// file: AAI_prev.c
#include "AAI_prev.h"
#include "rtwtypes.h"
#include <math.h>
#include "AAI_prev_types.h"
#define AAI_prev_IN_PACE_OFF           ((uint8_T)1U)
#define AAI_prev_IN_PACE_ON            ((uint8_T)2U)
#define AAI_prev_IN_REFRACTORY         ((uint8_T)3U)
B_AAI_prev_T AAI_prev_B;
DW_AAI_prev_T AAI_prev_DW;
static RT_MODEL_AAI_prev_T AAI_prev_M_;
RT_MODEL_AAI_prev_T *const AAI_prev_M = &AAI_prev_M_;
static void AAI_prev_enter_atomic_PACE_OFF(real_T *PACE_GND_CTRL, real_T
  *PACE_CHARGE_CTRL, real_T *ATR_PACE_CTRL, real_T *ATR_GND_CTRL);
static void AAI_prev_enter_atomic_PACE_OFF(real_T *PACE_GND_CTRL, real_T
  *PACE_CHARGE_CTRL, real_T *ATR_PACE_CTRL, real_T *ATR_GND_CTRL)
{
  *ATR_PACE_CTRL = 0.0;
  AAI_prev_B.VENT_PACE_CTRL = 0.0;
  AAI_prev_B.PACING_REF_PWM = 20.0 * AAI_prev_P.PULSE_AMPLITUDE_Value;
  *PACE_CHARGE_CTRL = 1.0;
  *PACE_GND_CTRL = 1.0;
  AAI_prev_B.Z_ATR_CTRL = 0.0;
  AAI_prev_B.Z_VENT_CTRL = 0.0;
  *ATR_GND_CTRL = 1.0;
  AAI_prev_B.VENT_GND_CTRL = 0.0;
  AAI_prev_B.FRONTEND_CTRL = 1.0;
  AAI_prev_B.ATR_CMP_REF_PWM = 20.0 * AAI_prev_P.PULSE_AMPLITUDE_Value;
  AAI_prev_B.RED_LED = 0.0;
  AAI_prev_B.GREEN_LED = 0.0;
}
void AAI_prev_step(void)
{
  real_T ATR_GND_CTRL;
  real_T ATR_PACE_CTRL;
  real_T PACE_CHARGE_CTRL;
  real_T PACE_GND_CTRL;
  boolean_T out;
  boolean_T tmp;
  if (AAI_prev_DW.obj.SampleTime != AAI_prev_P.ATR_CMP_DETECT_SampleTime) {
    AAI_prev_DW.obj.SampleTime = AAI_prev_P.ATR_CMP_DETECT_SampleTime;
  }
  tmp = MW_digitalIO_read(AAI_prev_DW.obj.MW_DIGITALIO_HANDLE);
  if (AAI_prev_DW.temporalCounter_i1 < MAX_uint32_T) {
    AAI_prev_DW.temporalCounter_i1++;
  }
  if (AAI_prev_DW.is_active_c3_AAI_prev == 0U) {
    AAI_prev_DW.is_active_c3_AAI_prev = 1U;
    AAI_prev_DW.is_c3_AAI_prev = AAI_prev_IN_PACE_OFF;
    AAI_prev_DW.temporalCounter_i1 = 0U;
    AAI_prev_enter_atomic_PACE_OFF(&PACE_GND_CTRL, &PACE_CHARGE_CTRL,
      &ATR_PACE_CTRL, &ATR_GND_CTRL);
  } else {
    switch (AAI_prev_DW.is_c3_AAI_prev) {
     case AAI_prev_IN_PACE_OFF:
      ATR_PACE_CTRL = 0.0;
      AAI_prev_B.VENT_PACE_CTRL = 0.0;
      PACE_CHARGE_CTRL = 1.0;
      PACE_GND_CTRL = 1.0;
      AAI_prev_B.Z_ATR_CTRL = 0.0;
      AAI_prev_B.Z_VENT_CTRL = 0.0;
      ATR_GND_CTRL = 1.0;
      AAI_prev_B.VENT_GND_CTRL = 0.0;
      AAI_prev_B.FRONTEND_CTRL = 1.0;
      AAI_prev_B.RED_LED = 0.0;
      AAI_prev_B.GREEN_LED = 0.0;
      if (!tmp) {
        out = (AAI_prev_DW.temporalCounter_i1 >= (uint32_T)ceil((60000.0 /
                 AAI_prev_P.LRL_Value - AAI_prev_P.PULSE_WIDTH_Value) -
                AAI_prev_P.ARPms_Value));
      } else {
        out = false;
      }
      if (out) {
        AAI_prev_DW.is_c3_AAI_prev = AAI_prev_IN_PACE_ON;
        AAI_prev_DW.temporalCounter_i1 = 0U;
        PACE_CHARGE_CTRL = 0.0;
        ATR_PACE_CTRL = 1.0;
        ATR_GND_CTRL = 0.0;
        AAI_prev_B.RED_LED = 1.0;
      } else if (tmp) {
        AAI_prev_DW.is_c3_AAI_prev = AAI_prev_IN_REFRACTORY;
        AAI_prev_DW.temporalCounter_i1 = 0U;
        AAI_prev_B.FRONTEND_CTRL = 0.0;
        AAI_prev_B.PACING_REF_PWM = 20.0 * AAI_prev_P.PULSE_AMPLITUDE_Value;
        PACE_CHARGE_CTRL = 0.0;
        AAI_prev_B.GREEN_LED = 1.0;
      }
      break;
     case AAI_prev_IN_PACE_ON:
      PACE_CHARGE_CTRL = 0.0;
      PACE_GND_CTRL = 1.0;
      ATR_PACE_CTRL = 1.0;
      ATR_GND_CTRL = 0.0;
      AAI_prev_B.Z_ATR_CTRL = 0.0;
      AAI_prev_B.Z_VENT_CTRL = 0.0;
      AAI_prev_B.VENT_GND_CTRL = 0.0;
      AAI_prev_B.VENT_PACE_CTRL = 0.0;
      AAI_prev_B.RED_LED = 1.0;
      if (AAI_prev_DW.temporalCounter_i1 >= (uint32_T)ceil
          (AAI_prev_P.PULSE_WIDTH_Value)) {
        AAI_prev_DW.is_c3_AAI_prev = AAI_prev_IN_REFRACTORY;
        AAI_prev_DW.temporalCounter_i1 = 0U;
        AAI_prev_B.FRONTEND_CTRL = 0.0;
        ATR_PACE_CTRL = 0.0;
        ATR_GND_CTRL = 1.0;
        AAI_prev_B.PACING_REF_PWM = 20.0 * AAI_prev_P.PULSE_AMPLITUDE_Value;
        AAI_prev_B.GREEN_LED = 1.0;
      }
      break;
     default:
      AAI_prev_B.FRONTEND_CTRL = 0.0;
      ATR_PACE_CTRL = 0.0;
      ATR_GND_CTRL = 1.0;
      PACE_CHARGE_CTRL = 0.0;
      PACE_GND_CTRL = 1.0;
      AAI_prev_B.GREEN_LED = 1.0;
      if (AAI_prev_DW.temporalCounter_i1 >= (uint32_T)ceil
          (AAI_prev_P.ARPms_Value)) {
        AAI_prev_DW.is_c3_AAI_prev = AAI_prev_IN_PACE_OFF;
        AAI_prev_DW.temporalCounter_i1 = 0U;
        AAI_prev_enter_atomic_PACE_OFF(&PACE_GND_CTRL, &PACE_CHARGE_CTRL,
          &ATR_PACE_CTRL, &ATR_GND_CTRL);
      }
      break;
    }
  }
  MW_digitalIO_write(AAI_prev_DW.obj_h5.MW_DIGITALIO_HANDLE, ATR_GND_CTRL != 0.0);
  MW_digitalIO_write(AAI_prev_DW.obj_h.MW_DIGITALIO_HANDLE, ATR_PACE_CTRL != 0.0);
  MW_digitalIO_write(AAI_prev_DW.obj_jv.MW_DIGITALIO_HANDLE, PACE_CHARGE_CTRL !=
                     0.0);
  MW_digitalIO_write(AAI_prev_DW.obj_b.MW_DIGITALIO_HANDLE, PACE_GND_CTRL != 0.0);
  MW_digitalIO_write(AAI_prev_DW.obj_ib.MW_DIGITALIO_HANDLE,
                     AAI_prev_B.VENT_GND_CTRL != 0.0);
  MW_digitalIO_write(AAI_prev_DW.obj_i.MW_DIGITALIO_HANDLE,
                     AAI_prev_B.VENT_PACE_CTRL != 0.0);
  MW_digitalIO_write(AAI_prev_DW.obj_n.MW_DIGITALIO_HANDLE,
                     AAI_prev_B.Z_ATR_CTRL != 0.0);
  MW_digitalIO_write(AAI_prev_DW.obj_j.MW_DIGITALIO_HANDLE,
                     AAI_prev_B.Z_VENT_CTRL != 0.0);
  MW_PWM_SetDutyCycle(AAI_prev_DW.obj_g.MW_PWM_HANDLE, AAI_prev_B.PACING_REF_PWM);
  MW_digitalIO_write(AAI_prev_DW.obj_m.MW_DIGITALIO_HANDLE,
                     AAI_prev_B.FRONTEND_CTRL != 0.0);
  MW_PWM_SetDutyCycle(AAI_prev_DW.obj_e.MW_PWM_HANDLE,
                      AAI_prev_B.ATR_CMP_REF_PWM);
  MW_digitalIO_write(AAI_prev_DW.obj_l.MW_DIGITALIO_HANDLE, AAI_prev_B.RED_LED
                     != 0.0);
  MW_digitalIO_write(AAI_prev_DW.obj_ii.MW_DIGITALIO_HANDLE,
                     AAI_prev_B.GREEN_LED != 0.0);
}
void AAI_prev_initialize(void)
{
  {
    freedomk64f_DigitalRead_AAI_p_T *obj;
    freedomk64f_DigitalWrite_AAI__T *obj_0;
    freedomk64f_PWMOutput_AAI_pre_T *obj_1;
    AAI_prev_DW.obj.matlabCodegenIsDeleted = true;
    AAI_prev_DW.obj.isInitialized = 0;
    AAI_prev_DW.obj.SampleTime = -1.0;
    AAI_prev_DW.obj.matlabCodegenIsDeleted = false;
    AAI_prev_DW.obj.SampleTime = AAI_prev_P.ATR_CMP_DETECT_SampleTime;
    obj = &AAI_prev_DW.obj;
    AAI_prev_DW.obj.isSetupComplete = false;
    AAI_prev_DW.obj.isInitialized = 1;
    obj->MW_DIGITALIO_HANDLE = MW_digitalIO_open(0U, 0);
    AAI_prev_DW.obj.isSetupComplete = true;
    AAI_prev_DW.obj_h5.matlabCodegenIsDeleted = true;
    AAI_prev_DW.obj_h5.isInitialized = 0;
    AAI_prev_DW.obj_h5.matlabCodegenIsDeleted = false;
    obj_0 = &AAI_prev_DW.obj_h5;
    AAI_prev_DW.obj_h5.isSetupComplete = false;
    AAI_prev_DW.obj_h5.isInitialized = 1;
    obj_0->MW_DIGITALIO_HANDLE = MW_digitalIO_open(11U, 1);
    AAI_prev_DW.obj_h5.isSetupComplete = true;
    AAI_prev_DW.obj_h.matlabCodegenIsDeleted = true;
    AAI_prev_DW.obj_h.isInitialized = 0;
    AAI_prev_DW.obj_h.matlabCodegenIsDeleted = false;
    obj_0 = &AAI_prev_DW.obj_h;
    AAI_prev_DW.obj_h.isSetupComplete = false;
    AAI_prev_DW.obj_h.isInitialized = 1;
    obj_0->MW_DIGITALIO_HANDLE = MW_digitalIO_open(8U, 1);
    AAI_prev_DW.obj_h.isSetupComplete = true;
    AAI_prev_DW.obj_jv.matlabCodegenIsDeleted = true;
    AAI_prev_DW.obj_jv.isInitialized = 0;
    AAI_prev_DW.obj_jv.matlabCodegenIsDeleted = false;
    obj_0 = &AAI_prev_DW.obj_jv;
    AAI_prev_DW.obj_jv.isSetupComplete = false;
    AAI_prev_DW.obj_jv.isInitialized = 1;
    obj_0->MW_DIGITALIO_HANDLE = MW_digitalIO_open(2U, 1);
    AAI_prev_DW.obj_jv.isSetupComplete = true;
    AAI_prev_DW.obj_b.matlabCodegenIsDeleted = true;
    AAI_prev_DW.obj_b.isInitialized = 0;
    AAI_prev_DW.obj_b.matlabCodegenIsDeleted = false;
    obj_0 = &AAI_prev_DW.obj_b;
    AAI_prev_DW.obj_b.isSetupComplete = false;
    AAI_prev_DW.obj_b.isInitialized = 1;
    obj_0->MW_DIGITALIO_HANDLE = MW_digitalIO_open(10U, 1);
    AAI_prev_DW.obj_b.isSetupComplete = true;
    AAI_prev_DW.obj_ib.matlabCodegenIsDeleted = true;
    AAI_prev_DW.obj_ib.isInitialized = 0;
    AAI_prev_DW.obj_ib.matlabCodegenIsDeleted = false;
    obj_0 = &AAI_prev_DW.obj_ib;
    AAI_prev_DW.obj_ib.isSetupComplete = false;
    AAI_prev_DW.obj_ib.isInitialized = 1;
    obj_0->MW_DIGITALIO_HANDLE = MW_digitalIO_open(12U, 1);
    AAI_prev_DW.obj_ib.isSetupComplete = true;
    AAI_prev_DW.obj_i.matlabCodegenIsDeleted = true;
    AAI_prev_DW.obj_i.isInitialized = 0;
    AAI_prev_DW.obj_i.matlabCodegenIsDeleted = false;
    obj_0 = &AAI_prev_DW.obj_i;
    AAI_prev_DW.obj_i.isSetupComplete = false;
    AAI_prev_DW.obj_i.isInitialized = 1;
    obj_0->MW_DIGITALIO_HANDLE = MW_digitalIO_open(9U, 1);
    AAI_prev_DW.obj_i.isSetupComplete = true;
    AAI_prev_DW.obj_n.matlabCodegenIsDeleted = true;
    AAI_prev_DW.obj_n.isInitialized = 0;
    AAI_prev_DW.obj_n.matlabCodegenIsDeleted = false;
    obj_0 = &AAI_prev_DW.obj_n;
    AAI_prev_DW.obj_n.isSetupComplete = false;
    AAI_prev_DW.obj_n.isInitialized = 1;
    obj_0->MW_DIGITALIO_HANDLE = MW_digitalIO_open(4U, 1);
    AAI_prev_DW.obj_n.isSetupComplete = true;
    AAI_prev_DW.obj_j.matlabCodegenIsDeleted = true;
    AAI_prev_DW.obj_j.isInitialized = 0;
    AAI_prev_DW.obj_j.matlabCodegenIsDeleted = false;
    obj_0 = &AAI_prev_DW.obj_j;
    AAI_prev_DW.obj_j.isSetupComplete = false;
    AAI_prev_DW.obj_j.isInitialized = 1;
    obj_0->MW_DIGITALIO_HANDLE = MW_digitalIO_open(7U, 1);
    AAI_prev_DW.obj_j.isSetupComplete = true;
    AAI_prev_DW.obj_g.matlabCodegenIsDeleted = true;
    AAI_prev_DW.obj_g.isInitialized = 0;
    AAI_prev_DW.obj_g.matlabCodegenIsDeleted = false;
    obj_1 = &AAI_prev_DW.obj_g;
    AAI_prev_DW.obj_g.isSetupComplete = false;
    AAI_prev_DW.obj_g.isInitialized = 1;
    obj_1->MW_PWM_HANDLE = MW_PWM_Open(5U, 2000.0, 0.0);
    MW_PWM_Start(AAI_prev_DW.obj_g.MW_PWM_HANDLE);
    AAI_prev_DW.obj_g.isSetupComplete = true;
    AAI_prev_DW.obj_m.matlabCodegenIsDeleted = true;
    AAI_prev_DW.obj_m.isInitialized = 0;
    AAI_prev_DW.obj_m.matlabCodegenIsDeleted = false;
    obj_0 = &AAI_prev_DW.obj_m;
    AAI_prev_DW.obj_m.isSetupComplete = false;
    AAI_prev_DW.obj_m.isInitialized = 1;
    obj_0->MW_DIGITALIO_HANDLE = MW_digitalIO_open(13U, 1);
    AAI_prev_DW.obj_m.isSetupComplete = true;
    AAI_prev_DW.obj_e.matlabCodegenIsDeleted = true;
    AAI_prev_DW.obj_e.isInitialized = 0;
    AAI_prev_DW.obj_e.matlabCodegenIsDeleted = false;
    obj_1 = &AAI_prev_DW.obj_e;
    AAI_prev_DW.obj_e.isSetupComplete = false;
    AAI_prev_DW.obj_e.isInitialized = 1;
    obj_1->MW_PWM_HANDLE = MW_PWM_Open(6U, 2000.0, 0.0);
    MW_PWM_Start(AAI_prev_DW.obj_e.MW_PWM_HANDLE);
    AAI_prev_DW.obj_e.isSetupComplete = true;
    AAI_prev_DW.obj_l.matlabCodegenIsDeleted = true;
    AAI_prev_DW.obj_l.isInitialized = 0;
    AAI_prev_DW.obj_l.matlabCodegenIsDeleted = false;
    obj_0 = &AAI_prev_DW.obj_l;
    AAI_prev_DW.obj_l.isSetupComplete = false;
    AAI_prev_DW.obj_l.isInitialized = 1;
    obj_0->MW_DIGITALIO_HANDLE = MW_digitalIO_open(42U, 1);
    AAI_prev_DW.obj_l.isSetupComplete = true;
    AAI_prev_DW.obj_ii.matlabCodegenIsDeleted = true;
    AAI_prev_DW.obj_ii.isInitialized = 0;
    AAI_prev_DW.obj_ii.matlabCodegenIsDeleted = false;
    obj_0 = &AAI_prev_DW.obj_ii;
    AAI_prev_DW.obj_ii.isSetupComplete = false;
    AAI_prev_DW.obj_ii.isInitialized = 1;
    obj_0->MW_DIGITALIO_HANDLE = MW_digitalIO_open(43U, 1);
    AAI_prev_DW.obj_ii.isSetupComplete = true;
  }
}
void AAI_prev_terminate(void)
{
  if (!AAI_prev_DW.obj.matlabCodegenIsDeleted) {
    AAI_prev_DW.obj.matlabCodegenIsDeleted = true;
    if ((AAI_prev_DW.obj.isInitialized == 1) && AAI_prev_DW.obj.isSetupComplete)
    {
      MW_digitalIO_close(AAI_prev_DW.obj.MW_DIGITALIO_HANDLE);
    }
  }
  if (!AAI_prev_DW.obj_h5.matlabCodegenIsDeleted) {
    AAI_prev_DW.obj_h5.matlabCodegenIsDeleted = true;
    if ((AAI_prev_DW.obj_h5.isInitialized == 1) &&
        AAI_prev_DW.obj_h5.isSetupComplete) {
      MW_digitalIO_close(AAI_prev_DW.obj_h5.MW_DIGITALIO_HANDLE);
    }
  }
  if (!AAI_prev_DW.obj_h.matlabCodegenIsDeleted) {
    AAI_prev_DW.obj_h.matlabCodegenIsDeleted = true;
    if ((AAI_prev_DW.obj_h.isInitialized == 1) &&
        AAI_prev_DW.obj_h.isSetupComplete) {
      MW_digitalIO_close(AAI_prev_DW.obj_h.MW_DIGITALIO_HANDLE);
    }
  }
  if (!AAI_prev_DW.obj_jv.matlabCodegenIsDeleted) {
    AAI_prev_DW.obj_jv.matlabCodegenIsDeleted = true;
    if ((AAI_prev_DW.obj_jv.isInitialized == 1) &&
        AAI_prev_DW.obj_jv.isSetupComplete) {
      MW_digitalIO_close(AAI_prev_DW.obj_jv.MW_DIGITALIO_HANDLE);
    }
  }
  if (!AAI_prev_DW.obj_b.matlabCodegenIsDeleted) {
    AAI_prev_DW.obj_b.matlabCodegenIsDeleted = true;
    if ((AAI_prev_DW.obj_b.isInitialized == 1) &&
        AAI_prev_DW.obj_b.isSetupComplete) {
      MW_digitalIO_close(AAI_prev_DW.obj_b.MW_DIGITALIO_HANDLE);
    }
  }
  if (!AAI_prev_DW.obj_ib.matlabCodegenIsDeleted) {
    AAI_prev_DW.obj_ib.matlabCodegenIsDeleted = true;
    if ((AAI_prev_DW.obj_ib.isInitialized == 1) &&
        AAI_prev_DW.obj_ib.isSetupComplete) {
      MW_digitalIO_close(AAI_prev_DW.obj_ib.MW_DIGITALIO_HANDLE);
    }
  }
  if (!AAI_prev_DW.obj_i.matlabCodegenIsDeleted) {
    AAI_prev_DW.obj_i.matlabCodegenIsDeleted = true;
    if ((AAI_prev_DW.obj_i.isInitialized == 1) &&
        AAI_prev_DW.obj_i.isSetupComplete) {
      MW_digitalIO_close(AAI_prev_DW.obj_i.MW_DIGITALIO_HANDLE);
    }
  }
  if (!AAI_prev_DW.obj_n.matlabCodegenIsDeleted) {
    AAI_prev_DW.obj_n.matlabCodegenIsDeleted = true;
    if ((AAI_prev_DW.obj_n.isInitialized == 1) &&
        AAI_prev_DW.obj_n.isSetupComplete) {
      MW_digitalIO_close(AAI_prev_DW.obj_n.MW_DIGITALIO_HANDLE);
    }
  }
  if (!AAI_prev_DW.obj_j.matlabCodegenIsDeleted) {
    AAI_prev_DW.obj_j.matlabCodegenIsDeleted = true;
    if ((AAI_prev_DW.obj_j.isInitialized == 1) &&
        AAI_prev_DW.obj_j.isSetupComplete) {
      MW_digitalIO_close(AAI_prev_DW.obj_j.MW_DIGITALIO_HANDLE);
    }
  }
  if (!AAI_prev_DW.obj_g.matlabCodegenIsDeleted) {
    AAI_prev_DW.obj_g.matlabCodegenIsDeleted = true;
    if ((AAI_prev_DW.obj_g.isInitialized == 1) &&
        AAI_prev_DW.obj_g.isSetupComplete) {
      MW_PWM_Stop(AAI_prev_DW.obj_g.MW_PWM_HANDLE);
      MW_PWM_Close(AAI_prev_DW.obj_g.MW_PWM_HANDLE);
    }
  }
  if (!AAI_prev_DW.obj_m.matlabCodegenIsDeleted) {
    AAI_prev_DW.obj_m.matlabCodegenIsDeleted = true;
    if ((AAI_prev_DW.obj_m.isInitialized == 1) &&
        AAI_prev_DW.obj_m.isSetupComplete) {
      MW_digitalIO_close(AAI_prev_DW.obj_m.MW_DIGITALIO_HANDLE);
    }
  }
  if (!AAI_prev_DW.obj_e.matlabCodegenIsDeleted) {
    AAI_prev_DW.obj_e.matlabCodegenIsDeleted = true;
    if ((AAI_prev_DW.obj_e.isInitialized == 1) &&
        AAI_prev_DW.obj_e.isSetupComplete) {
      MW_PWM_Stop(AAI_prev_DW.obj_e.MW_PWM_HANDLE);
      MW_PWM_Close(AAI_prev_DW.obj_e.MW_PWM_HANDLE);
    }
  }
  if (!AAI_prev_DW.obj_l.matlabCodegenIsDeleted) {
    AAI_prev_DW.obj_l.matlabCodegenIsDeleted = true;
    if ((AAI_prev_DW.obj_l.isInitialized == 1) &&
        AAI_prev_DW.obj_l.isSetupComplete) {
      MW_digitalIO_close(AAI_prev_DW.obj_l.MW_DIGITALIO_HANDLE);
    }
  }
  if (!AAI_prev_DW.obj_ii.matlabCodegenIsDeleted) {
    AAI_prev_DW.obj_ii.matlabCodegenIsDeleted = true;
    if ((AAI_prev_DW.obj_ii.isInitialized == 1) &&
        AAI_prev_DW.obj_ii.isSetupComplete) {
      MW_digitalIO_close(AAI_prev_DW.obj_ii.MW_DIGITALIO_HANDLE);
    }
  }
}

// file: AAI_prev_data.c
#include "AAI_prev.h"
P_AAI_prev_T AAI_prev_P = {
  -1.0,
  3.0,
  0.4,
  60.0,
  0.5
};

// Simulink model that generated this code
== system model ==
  ATR_GND_CTRL : frdmk64flib/Digital Write  <- 1: Stateflowchart#1
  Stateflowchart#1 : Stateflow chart  <- 1: PULSE_AMPLITUDE, 2: PULSE_WIDTH, 3: ATR_CMP_DETECT, 4: LRL, 5: ARPms
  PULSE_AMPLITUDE : Constant  Value=3
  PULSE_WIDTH : Constant  Value=0.4
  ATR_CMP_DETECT : frdmk64flib/Digital Read
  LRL : Constant  Value=60
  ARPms : Constant  Value=0.5
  ATR_PACE_CTRL : frdmk64flib/Digital Write  <- 1: Stateflowchart#1/2
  PACE_CHARGE_CTRL : frdmk64flib/Digital Write  <- 1: Stateflowchart#1/3
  PACE_GND_CTRL : frdmk64flib/Digital Write  <- 1: Stateflowchart#1/4
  VENT_GND_CTRL : frdmk64flib/Digital Write  <- 1: Stateflowchart#1/5
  VENT_PACE_CTRL : frdmk64flib/Digital Write  <- 1: Stateflowchart#1/6
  Z_ATR_CTRL : frdmk64flib/Digital Write  <- 1: Stateflowchart#1/7
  Z_VENT_CTRL : frdmk64flib/Digital Write  <- 1: Stateflowchart#1/8
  PACING_REF_PWM : frdmk64flib/PWM Output  <- 1: Stateflowchart#1/9
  FRONTEND_CTRL : frdmk64flib/Digital Write  <- 1: Stateflowchart#1/10
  ATR_CMP_REF_PWM : frdmk64flib/PWM Output  <- 1: Stateflowchart#1/11
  RED_LED : frdmk64flib/Digital Write  <- 1: Stateflowchart#1/12
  GREEN_LED : frdmk64flib/Digital Write  <- 1: Stateflowchart#1/13
== stateflow chart Stateflowchart#1 ==
  state PACE_OFF
    entry:
    ATR_PACE_CTRL = 0
    VENT_PACE_CTRL = 0
    PACING_REF_PWM = 20*PULSE_AMPLITUDE
    PACE_CHARGE_CTRL = 1
    PACE_GND_CTRL = 1
    Z_ATR_CTRL = 0
    Z_VENT_CTRL = 0
    ATR_GND_CTRL = 1
    VENT_GND_CTRL = 0
    FRONTEND_CTRL = 1
    ATR_CMP_REF_PWM = 20*PULSE_AMPLITUDE
    % light indicators
    RED_LED = 0
    GREEN_LED = 0
  state PACE_ON
    entry:
    PACE_CHARGE_CTRL = 0
    PACE_GND_CTRL = 1
    ATR_PACE_CTRL = 1
    ATR_GND_CTRL = 0
    Z_ATR_CTRL = 0
    Z_VENT_CTRL = 0
    VENT_GND_CTRL = 0
    VENT_PACE_CTRL = 0
    % light indicator
    RED_LED = 1
  note: at paceon state, the system waits for the atr_cmp_detect signal to decide which
      | mode to go to . if atr_cmp_detect == 0, pace on. else, go refractory mode.
  note: when pacing, after the pulse width,
      | the mode would change to refractory mdoe
  state REFRACTORY
    entry:
    FRONTEND_CTRL = 0
    ATR_PACE_CTRL = 0
    ATR_GND_CTRL = 1
    PACING_REF_PWM = 20*PULSE_AMPLITUDE
    PACE_CHARGE_CTRL = 0
    PACE_GND_CTRL = 1
    % light indicator
    GREEN_LED = 1
  (default) -> PACE_OFF
  PACE_OFF -> PACE_ON [order 1] : [(ATR_CMP_DETECT == 0) && after((60000/LRL)-PULSE_WIDTH-ARP,msec)]
  PACE_ON -> REFRACTORY : [after(PULSE_WIDTH,msec)]
  REFRACTORY -> PACE_OFF : [after(ARP,msec)]
  PACE_OFF -> REFRACTORY [order 2] : [ATR_CMP_DETECT == 1]
  data: ATR_GND_CTRL output; ATR_PACE_CTRL output; PACE_CHARGE_CTRL output; PACE_GND_CTRL output; VENT_GND_CTRL output; VENT_PACE_CTRL output; Z_ATR_CTRL output; Z_VENT_CTRL output; PULSE_AMPLITUDE input; PACING_REF_PWM output; FRONTEND_CTRL output; ATR_CMP_REF_PWM output; RED_LED output; PULSE_WIDTH input; ATR_CMP_DETECT input; GREEN_LED output; LRL input; ARP input
